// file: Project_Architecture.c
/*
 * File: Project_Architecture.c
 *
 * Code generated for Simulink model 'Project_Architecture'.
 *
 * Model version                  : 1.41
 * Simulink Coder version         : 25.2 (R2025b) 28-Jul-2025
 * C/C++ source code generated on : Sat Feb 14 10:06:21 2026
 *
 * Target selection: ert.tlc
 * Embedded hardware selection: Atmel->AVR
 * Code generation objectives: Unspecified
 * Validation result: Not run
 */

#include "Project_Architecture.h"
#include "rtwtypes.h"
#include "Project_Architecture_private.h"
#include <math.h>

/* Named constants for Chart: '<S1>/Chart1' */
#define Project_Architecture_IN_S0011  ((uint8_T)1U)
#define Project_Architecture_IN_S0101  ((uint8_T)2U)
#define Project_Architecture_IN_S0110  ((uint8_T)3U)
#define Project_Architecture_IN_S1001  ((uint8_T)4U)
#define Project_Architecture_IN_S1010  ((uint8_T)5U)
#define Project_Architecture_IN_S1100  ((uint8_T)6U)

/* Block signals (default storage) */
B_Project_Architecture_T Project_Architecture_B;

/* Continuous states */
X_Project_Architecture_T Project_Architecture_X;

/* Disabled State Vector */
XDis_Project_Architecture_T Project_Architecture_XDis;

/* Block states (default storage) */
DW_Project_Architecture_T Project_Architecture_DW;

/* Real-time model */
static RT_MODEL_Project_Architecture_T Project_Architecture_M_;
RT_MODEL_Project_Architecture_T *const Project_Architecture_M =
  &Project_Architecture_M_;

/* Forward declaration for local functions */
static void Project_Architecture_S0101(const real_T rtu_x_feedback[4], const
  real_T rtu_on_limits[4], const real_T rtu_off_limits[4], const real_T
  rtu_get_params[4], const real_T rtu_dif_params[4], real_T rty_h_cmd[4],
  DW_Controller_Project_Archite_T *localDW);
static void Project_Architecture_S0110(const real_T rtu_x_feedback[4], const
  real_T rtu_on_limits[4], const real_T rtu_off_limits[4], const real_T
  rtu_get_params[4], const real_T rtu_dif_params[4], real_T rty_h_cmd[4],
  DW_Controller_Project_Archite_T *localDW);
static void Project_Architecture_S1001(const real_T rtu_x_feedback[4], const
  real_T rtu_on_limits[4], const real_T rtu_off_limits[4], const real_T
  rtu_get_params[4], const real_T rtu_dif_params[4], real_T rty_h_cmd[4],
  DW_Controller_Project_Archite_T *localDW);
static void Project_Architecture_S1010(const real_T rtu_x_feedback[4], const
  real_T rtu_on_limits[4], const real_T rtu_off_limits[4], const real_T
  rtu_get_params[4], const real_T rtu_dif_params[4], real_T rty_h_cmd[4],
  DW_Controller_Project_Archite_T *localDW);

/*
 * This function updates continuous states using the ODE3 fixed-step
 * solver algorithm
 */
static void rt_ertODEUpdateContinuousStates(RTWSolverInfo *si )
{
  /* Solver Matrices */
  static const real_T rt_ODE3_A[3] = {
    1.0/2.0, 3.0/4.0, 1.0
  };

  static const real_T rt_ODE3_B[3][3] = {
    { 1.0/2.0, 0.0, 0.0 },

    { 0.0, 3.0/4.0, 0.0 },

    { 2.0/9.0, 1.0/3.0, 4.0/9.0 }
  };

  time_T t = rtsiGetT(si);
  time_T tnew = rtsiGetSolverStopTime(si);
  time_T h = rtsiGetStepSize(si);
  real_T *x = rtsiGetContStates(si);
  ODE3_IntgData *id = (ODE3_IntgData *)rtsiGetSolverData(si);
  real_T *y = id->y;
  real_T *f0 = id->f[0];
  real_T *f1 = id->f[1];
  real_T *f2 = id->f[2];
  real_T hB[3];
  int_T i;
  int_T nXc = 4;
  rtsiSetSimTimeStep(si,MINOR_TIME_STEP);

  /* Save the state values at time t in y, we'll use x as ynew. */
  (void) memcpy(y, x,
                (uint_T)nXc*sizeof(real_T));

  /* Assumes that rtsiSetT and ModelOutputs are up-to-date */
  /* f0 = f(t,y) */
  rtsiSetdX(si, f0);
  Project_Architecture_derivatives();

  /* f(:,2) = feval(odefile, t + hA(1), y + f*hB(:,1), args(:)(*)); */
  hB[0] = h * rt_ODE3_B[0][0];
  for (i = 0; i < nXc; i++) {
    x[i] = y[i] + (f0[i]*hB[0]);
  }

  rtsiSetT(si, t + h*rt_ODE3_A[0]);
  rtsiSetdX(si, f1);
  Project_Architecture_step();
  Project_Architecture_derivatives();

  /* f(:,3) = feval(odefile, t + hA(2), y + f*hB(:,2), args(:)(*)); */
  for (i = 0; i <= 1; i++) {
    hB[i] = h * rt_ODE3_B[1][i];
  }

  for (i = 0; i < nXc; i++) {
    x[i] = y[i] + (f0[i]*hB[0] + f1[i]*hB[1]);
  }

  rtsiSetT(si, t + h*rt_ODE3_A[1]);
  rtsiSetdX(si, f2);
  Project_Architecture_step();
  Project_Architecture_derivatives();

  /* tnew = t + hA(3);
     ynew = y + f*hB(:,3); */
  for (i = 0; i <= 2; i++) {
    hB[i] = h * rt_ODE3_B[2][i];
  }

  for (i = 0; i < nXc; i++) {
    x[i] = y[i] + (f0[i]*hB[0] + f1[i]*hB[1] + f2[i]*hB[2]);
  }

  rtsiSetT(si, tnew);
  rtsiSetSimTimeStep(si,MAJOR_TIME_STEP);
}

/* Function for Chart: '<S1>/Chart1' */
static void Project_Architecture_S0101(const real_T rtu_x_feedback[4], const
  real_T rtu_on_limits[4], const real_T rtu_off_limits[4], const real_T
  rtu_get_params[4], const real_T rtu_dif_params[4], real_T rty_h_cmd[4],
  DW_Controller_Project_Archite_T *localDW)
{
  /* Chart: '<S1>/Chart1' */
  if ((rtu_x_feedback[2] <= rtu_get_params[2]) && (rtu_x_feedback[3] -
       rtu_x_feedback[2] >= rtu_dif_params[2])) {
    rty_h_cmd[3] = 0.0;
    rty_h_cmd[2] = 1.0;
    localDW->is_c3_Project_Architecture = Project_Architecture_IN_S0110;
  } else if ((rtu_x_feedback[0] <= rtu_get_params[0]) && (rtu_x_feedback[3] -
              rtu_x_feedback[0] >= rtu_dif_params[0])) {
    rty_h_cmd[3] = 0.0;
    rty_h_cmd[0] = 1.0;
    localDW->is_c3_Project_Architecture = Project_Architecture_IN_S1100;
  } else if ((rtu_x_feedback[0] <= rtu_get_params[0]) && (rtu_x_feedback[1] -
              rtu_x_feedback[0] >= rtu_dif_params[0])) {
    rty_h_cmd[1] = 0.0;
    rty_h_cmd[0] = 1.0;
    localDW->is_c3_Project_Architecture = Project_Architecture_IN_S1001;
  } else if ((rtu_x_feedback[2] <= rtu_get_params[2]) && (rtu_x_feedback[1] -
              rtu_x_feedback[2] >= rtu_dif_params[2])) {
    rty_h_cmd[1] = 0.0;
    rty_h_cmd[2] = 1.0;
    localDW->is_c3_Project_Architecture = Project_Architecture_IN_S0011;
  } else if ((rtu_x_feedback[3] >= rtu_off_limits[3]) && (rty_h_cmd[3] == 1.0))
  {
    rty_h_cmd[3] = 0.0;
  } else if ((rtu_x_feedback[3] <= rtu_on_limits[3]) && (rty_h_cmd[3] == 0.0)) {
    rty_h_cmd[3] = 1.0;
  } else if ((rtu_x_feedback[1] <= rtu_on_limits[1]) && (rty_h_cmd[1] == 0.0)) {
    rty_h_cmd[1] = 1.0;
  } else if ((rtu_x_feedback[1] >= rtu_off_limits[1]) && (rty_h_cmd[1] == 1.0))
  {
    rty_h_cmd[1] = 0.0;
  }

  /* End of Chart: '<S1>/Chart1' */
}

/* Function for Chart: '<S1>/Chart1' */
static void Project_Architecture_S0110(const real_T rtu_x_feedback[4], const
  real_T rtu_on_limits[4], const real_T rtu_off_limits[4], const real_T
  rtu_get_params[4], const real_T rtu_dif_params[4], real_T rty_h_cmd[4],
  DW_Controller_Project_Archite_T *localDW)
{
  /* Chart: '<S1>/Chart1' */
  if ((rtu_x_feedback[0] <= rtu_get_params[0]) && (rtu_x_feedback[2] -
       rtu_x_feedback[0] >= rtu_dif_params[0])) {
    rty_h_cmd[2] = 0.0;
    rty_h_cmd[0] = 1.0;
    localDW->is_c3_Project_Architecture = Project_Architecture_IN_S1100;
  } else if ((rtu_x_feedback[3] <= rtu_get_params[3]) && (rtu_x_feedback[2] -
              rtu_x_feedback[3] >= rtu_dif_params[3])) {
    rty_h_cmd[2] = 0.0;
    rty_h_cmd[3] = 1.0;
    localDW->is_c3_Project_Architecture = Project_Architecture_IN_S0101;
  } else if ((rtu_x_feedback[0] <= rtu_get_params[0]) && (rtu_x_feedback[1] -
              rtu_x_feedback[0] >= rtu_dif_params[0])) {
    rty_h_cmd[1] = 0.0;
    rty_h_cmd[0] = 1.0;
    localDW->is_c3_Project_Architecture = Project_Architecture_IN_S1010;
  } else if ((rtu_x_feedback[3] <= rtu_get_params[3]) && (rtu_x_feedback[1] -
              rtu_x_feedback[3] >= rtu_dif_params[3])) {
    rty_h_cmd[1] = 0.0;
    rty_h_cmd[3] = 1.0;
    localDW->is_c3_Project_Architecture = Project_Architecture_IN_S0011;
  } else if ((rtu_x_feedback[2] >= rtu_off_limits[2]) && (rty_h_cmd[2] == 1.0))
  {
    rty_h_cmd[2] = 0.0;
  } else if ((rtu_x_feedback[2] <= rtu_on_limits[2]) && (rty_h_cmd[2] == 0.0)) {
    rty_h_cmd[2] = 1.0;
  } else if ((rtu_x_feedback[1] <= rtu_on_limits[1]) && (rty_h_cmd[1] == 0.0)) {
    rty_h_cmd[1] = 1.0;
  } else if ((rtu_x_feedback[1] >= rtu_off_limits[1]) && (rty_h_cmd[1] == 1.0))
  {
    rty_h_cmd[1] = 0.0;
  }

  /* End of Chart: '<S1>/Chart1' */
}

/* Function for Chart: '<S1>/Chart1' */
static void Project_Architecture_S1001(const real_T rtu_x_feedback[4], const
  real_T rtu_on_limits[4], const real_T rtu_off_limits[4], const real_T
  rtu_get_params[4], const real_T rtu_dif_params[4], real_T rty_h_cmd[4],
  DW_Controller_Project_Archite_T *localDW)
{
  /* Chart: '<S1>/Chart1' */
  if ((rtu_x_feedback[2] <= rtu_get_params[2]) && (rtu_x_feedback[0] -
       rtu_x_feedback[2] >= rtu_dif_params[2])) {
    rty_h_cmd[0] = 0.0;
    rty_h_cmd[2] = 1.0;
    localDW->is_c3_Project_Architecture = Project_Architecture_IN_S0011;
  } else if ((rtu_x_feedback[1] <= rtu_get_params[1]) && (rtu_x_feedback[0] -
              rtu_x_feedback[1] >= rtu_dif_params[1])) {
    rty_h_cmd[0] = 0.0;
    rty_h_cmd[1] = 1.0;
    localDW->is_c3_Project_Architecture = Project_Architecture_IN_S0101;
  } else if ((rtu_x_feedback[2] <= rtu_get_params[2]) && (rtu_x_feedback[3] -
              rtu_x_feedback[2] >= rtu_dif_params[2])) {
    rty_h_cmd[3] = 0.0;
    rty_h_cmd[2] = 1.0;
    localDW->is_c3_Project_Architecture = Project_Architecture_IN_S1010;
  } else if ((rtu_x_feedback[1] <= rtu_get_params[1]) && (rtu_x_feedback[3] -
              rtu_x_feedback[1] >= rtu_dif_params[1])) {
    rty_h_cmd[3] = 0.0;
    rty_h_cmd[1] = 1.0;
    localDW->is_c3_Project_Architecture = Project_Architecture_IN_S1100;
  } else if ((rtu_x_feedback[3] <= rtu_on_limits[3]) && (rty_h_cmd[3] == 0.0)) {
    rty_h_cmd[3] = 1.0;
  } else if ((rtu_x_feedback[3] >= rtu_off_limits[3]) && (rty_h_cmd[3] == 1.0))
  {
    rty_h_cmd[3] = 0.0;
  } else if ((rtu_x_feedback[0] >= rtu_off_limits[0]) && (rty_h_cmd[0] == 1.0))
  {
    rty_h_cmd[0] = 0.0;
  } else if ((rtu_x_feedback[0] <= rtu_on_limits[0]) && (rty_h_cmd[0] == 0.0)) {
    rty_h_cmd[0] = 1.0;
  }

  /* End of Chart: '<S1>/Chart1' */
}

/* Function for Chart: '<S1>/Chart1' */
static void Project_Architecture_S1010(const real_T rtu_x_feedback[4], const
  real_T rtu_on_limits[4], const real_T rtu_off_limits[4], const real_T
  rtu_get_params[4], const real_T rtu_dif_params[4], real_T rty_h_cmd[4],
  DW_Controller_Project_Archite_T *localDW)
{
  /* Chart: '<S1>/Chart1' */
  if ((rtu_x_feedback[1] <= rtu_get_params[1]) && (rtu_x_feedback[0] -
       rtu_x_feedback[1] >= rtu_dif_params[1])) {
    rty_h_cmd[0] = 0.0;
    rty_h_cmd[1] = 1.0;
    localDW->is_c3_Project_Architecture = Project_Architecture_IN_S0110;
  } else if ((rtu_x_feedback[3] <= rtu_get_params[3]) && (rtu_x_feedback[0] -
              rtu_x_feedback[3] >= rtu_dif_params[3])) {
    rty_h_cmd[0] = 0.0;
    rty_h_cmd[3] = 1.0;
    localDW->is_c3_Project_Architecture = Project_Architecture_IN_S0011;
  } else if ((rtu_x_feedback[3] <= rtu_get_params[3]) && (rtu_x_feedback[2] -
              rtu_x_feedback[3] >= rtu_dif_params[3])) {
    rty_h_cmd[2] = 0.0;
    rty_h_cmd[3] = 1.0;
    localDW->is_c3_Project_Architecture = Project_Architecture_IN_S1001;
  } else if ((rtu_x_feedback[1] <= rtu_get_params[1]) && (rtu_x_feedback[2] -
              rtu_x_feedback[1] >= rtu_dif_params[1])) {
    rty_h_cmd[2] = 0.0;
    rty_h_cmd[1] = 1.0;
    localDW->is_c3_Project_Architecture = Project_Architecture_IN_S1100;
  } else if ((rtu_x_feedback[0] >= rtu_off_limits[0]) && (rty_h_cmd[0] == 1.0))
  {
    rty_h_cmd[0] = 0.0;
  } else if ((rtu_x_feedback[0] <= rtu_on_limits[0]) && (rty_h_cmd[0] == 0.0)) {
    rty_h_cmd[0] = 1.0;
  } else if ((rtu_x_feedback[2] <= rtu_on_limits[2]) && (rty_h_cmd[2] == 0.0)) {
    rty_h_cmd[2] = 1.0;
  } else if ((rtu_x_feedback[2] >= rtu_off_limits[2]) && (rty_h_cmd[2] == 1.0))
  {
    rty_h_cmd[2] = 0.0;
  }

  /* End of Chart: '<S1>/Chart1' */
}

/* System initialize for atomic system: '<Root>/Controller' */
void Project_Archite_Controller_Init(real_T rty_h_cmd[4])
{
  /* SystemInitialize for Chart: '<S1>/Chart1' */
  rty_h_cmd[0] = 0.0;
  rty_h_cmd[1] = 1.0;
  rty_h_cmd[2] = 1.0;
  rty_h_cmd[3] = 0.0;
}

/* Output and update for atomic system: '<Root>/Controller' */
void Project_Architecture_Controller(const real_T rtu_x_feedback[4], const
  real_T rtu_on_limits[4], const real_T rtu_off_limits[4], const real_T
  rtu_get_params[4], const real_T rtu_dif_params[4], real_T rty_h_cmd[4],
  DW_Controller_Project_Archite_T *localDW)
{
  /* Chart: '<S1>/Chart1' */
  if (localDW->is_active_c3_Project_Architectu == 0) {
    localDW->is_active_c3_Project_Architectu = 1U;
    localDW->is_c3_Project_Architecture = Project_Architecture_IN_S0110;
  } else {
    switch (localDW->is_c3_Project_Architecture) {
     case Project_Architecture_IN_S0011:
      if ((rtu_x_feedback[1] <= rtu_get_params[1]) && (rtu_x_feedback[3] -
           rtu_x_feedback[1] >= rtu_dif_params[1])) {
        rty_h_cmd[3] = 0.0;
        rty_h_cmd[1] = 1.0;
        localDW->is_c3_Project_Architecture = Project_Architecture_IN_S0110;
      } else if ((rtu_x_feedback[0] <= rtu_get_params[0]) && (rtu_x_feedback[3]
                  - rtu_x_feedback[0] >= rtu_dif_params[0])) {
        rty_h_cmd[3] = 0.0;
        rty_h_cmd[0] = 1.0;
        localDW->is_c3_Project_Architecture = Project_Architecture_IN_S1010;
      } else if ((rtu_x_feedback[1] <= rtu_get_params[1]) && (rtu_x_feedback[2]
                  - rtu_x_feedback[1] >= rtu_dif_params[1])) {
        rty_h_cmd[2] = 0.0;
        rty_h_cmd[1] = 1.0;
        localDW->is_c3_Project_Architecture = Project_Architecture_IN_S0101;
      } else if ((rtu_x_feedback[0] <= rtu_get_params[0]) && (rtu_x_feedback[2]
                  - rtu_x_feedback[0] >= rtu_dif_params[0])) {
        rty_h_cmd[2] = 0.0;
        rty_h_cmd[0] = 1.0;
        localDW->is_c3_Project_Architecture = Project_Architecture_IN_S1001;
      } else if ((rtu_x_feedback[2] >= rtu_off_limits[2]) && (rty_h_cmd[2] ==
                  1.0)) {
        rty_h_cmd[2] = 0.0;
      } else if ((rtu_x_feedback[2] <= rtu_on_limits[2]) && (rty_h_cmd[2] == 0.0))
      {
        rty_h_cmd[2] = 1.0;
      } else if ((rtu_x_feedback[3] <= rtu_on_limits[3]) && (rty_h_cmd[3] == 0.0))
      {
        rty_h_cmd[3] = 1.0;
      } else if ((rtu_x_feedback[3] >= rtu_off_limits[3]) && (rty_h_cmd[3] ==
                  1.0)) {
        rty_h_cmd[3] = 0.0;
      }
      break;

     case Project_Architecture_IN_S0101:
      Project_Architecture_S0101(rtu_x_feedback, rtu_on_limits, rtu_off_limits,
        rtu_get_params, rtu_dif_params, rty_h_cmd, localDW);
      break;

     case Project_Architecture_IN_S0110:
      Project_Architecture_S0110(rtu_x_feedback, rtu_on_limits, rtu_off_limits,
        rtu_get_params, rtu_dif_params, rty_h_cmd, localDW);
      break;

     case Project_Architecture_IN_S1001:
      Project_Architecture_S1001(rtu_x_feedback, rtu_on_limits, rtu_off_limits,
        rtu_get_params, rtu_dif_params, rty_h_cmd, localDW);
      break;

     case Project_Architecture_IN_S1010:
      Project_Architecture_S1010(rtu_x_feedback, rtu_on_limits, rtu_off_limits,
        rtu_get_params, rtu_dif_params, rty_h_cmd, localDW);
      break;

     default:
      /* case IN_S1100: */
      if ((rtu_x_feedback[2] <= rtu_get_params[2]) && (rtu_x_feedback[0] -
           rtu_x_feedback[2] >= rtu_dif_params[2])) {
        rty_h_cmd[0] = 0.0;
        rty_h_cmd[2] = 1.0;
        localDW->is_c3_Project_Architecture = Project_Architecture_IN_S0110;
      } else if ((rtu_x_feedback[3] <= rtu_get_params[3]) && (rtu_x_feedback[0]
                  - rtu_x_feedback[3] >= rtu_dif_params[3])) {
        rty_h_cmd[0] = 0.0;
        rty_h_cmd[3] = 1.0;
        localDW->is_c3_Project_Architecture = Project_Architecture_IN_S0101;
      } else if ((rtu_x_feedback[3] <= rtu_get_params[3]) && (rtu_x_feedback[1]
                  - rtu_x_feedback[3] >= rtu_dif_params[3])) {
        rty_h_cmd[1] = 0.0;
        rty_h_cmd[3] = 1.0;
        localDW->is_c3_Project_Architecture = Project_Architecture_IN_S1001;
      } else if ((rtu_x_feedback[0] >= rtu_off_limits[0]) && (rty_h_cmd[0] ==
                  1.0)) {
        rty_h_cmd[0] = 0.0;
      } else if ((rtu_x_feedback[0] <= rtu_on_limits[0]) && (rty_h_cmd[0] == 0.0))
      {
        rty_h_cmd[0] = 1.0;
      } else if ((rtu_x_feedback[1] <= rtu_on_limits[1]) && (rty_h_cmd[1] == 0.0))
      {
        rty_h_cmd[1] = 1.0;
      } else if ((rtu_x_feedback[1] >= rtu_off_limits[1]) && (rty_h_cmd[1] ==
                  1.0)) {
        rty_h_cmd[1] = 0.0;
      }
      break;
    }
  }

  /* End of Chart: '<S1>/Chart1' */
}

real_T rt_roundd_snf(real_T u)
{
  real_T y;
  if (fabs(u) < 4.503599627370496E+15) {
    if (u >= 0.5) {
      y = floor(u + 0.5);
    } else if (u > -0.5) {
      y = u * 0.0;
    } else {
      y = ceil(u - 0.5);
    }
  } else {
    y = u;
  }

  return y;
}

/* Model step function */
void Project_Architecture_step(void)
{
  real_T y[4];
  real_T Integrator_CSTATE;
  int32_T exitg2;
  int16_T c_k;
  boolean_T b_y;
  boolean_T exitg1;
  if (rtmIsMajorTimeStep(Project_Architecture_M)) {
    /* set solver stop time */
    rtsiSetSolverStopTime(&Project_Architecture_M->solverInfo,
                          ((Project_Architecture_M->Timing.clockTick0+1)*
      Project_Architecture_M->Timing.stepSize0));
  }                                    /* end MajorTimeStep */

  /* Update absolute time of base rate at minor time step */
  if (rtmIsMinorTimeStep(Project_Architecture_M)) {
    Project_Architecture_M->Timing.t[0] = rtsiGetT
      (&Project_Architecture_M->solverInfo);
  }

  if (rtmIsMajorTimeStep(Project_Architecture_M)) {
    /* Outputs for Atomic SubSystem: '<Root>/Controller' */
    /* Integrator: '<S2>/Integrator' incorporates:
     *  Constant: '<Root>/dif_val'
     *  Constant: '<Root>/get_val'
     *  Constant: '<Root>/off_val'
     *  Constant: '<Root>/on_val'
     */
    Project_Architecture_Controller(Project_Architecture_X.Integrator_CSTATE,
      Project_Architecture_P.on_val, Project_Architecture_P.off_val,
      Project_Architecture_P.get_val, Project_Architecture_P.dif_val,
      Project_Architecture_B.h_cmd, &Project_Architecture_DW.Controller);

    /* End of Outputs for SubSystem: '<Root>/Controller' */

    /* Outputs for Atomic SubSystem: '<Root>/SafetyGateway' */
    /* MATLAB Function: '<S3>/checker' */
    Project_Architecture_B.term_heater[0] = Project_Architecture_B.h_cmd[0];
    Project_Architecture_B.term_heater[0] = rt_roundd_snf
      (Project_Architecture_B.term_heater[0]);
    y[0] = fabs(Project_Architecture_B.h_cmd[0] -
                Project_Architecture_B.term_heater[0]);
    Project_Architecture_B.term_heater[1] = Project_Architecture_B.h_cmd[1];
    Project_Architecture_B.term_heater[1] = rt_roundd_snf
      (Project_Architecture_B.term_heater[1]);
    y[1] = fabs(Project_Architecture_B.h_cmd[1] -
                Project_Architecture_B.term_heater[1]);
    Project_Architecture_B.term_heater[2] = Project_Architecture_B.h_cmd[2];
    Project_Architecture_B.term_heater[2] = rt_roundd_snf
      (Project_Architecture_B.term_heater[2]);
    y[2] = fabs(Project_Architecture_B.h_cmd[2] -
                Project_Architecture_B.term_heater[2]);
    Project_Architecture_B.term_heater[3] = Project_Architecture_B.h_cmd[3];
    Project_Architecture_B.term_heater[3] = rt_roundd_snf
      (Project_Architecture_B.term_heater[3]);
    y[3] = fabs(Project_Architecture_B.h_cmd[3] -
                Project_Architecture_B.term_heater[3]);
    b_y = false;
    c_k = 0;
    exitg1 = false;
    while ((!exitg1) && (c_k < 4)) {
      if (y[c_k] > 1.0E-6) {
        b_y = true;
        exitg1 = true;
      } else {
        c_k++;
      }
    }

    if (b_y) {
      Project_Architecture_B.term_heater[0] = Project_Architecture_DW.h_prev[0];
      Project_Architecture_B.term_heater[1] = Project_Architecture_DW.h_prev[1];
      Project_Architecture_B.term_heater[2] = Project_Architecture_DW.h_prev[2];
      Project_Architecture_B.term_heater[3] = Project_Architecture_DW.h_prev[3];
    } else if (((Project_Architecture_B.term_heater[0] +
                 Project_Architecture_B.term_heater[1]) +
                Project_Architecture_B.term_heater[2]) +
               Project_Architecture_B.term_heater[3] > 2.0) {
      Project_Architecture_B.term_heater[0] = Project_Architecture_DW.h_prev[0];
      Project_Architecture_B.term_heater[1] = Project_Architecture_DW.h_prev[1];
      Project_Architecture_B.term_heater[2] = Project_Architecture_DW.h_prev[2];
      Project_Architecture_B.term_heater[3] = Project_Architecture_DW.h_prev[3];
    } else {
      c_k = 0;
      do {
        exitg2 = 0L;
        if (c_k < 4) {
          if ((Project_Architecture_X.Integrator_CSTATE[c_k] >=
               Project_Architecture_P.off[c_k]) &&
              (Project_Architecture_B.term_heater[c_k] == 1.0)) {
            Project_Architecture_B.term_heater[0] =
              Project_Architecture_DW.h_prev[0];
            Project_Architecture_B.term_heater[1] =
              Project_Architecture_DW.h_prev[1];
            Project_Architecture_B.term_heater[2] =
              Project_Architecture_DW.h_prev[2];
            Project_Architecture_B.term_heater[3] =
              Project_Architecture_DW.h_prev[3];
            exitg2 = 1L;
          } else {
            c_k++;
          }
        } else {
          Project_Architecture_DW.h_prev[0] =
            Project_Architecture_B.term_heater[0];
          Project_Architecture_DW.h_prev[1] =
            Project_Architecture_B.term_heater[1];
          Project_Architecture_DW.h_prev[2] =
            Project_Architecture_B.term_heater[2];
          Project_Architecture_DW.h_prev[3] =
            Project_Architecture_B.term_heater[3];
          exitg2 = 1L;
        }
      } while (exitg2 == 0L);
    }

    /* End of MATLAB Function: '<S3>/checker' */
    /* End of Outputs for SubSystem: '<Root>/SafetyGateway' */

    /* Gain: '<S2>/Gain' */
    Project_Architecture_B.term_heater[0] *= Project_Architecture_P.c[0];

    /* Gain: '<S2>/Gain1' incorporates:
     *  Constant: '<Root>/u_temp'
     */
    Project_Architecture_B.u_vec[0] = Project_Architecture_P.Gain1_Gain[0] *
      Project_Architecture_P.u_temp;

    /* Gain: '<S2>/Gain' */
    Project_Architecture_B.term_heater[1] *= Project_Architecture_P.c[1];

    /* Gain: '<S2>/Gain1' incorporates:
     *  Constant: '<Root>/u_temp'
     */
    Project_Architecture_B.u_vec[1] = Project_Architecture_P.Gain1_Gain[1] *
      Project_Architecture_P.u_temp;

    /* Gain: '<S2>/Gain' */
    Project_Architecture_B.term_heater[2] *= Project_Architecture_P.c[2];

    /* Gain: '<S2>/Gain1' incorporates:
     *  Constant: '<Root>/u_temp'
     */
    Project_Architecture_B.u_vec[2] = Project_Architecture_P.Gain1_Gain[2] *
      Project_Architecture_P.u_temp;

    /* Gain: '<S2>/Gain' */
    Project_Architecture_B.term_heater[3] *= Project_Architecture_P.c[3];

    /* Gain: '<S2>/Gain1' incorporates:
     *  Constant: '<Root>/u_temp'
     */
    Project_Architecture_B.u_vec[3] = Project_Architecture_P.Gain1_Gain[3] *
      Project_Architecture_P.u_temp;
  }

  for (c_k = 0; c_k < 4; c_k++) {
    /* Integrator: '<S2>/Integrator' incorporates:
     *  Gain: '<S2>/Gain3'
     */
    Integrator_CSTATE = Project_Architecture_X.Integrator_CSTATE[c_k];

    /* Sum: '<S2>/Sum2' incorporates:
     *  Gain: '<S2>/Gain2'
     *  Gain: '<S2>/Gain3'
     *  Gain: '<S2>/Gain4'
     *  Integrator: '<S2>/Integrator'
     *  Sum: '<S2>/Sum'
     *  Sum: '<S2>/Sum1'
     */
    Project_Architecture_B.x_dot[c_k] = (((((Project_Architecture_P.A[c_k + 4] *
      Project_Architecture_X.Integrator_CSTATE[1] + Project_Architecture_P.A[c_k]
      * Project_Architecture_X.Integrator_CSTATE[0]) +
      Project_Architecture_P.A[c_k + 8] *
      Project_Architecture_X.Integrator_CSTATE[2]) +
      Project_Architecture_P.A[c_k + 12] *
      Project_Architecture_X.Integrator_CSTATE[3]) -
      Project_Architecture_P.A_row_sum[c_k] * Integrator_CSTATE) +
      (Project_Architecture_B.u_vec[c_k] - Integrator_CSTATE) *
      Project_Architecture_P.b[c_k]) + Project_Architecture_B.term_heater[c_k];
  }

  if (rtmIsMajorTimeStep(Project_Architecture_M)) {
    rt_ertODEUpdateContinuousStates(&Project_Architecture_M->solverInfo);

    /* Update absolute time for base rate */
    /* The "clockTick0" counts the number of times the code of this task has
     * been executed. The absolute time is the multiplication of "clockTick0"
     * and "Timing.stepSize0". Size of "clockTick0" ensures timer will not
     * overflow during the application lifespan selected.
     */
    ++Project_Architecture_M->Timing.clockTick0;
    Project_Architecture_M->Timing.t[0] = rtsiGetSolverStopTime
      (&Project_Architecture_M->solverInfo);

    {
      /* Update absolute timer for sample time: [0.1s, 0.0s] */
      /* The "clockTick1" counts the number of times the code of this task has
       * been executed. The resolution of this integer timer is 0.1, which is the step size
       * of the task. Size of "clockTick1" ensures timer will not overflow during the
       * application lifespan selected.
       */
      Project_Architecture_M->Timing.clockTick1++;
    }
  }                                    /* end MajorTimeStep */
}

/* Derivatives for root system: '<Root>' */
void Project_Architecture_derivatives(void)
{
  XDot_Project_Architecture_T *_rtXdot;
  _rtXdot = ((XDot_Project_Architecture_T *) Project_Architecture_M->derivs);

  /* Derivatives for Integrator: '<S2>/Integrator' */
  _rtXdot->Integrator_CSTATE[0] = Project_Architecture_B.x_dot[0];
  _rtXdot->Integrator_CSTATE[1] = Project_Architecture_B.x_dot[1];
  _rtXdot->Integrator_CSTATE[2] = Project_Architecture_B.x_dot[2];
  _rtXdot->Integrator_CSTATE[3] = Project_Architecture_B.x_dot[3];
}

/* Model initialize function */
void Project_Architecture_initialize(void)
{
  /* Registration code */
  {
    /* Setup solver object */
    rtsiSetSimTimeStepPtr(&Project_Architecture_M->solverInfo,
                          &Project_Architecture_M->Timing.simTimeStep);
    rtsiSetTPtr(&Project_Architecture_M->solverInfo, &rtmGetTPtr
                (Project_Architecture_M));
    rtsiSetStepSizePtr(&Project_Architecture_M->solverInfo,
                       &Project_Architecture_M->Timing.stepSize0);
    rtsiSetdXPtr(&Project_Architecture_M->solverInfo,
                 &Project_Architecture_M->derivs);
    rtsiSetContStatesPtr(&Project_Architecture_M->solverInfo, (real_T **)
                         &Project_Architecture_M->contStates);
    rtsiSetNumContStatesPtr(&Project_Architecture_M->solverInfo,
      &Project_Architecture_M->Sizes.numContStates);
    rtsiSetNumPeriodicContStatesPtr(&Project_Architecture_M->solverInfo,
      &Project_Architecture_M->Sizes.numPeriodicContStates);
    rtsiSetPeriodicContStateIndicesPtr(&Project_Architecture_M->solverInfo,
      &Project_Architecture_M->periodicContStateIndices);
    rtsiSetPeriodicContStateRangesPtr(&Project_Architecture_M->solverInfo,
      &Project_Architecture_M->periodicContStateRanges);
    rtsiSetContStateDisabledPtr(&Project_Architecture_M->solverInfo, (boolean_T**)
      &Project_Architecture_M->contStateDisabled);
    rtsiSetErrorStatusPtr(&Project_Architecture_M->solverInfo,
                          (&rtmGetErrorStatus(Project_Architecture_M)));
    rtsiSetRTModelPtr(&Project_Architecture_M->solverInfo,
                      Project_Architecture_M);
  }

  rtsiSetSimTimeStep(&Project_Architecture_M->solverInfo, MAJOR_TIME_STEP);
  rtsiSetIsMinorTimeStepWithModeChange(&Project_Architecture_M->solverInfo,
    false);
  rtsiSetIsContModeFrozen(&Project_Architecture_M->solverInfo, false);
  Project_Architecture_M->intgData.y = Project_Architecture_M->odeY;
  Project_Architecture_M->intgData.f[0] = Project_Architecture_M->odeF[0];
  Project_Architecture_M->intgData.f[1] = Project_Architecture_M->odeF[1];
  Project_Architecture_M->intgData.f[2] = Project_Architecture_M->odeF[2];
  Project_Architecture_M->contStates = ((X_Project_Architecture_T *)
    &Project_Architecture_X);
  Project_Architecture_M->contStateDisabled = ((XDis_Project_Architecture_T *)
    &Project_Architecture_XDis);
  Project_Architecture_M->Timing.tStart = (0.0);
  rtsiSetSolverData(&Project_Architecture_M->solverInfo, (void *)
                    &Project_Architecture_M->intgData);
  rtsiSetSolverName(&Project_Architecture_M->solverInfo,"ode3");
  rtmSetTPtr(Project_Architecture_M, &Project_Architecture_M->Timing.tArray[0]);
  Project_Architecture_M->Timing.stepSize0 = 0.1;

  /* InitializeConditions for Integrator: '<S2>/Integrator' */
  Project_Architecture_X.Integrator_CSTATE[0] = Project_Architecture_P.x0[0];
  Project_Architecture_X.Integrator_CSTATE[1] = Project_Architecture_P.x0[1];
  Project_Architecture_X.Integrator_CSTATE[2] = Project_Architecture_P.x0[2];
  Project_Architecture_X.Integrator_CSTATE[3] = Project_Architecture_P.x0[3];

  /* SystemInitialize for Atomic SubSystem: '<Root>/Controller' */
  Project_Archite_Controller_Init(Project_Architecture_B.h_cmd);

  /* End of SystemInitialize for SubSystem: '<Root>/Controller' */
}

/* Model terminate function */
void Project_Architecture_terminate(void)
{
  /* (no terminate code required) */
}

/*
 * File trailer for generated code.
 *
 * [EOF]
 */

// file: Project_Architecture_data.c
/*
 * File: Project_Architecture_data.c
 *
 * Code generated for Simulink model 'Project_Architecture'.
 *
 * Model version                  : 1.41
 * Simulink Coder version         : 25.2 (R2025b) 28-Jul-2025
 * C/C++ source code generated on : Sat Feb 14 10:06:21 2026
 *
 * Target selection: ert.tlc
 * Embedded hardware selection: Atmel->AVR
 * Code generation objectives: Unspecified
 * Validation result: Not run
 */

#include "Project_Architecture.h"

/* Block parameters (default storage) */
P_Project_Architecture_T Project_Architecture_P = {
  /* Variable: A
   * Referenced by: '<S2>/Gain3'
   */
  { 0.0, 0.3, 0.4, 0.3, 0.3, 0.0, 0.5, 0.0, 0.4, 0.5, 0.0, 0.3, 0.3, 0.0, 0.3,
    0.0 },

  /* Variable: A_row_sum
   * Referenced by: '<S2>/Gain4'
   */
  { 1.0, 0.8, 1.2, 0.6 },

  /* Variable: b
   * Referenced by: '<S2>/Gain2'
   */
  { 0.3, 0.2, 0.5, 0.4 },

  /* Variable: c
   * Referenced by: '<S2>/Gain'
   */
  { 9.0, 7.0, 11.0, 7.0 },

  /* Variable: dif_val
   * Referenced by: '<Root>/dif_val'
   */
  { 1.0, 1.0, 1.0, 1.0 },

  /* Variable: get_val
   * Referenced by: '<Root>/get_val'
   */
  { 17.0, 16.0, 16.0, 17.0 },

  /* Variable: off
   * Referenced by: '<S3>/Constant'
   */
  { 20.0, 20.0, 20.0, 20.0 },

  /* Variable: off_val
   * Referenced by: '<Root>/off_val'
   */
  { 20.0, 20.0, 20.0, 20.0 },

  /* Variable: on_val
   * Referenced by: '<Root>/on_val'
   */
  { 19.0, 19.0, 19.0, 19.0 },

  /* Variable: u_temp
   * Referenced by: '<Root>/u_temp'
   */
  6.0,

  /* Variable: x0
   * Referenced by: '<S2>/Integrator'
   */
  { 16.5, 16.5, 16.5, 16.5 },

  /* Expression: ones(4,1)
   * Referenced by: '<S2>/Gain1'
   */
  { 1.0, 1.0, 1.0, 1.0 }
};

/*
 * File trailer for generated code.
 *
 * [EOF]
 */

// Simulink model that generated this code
simulink model "Project_Architecture"  (R2025b)
settings: Solver=FixedStepAuto  StartTime=0.0  StopTime=200  FixedStep=0.1  RelTol=1e-3
values from neighbouring files (symbols this model uses):
  A = [0.00, 0.30, 0.40, 0.30 ... (first row only)    [init_params.m]
  A_row_sum = sum(A, 2)    [init_params.m]
  b = [0.30; 0.20; 0.50; 0.40]    [init_params.m]
  c = [9.00; 7.00; 11.00; 7.00]    [init_params.m]
  dif_val = dif    [init_params.m]
  get_val = get    [init_params.m]
  off_val = off    [init_params.m]
  on_val = on    [init_params.m]
  u_temp = 6    [init_params.m]
  x0 = [16.5; 16.5; 16.5; 16.5]    [init_params.m]

== system Project_Architecture ==
  Controller : Subsystem  TreatAsAtomicUnit=on  SystemSampleTime=0.1
  RoomModel : Subsystem
  SafetyGateway : Subsystem  TreatAsAtomicUnit=on  SystemSampleTime=0.1
  Scope : Scope  NumInputPorts=4
  dif_val : Constant  Value=dif_val
  get_val : Constant  Value=get_val
  off_val : Constant  Value=off_val
  on_val : Constant  Value=on_val
  u_temp : Constant  Value=u_temp
  wires:
  u_temp/1 -> RoomModel/1(u_temp)
  SafetyGateway/1(h_act) -> RoomModel/2(h_act), Scope/3  "Heaters <4>"
  RoomModel/1(x_temp) -> Scope/1, SafetyGateway/1(x_temp), Controller/1(x_feedback)  "Temperature <4>"
  Controller/1(h_cmd) -> SafetyGateway/2(h_cmd), Scope/2
  SafetyGateway/2(unsafe_flag) -> Scope/4
  on_val/1 -> Controller/2(on_limits)
  off_val/1 -> Controller/3(off_limits)
  get_val/1 -> Controller/4(get_params)
  dif_val/1 -> Controller/5(dif_params)

== system Project_Architecture/Controller ==
  x_feedback : Inport
  on_limits : Inport  Port=2
  off_limits : Inport  Port=3
  get_params : Inport  Port=4
  dif_params : Inport  Port=5
  Chart1 : Stateflow chart  TreatAsAtomicUnit=on
  h_cmd : Outport
  h : Outport  Port=2
  wires:
  x_feedback/1 -> Chart1/1(x_feedback)
  Chart1/1(h_cmd) -> h_cmd/1
  off_limits/1 -> Chart1/3(off_limits)
  get_params/1 -> Chart1/4(get_params)
  dif_params/1 -> Chart1/5(dif_params)
  on_limits/1 -> Chart1/2(on_limits)

== system Project_Architecture/RoomModel ==
  u_temp : Inport  PortDimensions=1
  h_act : Inport  Port=2  PortDimensions=4
  Gain : Gain  Gain=c
  Gain1 : Gain  Gain=ones(4,1)
  Gain2 : Gain  Gain=b
  Gain3 : Gain  Gain=A  Multiplication=Matrix(K*u)
  Gain4 : Gain  Gain=A_row_sum
  Integrator : Integrator  InitialCondition=x0
  Sum : Sum  Inputs=|+-
  Sum1 : Sum  Inputs=|+-
  Sum2 : Sum  Inputs=|+++
  x_temp : Outport  PortDimensions=4
  wires:
  u_temp/1 -> Gain1/1
  h_act/1 -> Gain/1
  Gain/1 -> Sum2/3  "term_heater"
  Gain1/1 -> Sum/1  "u_vec"
  Sum/1 -> Gain2/1
  Gain4/1 -> Sum1/2  "Axi"
  Gain3/1 -> Sum1/1  "Ax"
  Sum1/1 -> Sum2/1  "term_neighbors"
  Gain2/1 -> Sum2/2  "term_outside"
  Sum2/1 -> Integrator/1  "x_dot"
  Integrator/1 -> x_temp/1, [A1]
  [A1] -> Gain3/1
  [A1] -> Sum/2
  [A1] -> Gain4/1

== system Project_Architecture/SafetyGateway ==
  x_temp : Inport  PortDimensions=4
  h_cmd : Inport  Port=2  PortDimensions=4
  Constant : Constant  Value=off
  checker : MATLAB Function  TreatAsAtomicUnit=on
  h_act : Outport  PortDimensions=4
  unsafe_flag : Outport  Port=2  PortDimensions=1
  wires:
  x_temp/1 -> checker/1(x_temp)
  h_cmd/1 -> checker/2(h_cmd)
  checker/1(h_act) -> h_act/1
  checker/2(unsafe_flag) -> unsafe_flag/1
  Constant/1 -> checker/3(off)

== matlab function Project_Architecture/SafetyGateway/checker ==
function [h_act, unsafe_flag] = checker(x_temp, h_cmd, off)

persistent h_prev
if isempty(h_prev)
    h_prev = zeros(4,1);
end

unsafe_flag = 0;

% Force column vectors
x = x_temp(:);
h = h_cmd(:);

h_rounded = round(h);

if any(abs(h - h_rounded) > 1e-6)
    unsafe_flag = 1;
    h_act = h_prev;
    return;
end

h = h_rounded;

if sum(h) > 2
    unsafe_flag = 1;
    h_act = h_prev;
    return;
end

for i = 1:4
    if x(i) >= off(i) && h(i) == 1
        unsafe_flag = 1;
        h_act = h_prev;
        return;
    end
end

h_act = h;
h_prev = h_act;

== stateflow chart Project_Architecture/Controller/Chart1 ==
  settings: sampleTime=0.01
  state S1100
    state S3
    (default) -> S1100.S3
    S1100.S3 -> S1100.S3 [order 4] : [x_feedback(2)>=off_limits(2) && h_cmd(2) == 1]{h_cmd(2) = 0;}
    S1100.S3 -> S1100.S3 [order 3] : [x_feedback(2) <=on_limits(2) && h_cmd(2) == 0]{h_cmd(2) = 1;}
    S1100.S3 -> S1100.S3 [order 2] : [x_feedback(1) <=on_limits(1) && h_cmd(1) == 0]{h_cmd(1) = 1;}
    S1100.S3 -> S1100.S3 [order 1] : [x_feedback(1)>=off_limits(1) && h_cmd(1) == 1]{h_cmd(1) = 0;}
  state S0110
    state S3
    (default) -> S0110.S3
    S0110.S3 -> S0110.S3 [order 4] : [x_feedback(2)>=off_limits(2) && h_cmd(2) == 1]{h_cmd(2) = 0;}
    S0110.S3 -> S0110.S3 [order 3] : [x_feedback(2) <=on_limits(2) && h_cmd(2) == 0]{h_cmd(2) = 1;}
    S0110.S3 -> S0110.S3 [order 2] : [x_feedback(3) <=on_limits(3) && h_cmd(3) == 0]{h_cmd(3) = 1;}
    S0110.S3 -> S0110.S3 [order 1] : [x_feedback(3)>=off_limits(3) && h_cmd(3) == 1]{h_cmd(3) = 0;}
  state S0101
    state S3
    (default) -> S0101.S3
    S0101.S3 -> S0101.S3 [order 4] : [x_feedback(2)>=off_limits(2) && h_cmd(2) == 1]{h_cmd(2) = 0;}
    S0101.S3 -> S0101.S3 [order 3] : [x_feedback(2) <=on_limits(2) && h_cmd(2) == 0]{h_cmd(2) = 1;}
    S0101.S3 -> S0101.S3 [order 2] : [x_feedback(4) <=on_limits(4) && h_cmd(4) == 0]{h_cmd(4) = 1;}
    S0101.S3 -> S0101.S3 [order 1] : [x_feedback(4)>=off_limits(4) && h_cmd(4) == 1]{h_cmd(4) = 0;}
  state S0011
    state S3
    S0011.S3 -> S0011.S3 [order 4] : [x_feedback(4)>=off_limits(4) && h_cmd(4) == 1]{h_cmd(4) = 0;}
    S0011.S3 -> S0011.S3 [order 3] : [x_feedback(4) <=on_limits(4) && h_cmd(4) == 0]{h_cmd(4) = 1;}
    S0011.S3 -> S0011.S3 [order 2] : [x_feedback(3) <=on_limits(3) && h_cmd(3) == 0]{h_cmd(3) = 1;}
    S0011.S3 -> S0011.S3 [order 1] : [x_feedback(3)>=off_limits(3) && h_cmd(3) == 1]{h_cmd(3) = 0;}
  state S1001
    state S3
    (default) -> S1001.S3
    S1001.S3 -> S1001.S3 [order 2] : [x_feedback(4)>=off_limits(4) && h_cmd(4) == 1]{h_cmd(4) = 0;}
    S1001.S3 -> S1001.S3 [order 1] : [x_feedback(4) <=on_limits(4) && h_cmd(4) == 0]{h_cmd(4) = 1;}
    S1001.S3 -> S1001.S3 [order 4] : [x_feedback(1) <=on_limits(1) && h_cmd(1) == 0]{h_cmd(1) = 1;}
    S1001.S3 -> S1001.S3 [order 3] : [x_feedback(1)>=off_limits(1) && h_cmd(1) == 1]{h_cmd(1) = 0;}
  state S1010
    state S3
    (default) -> S1010.S3
    S1010.S3 -> S1010.S3 [order 4] : [x_feedback(3)>=off_limits(3) && h_cmd(3) == 1]{h_cmd(3) = 0;}
    S1010.S3 -> S1010.S3 [order 3] : [x_feedback(3) <=on_limits(3) && h_cmd(3) == 0]{h_cmd(3) = 1;}
    S1010.S3 -> S1010.S3 [order 2] : [x_feedback(1) <=on_limits(1) && h_cmd(1) == 0]{h_cmd(1) = 1;}
    S1010.S3 -> S1010.S3 [order 1] : [x_feedback(1)>=off_limits(1) && h_cmd(1) == 1]{h_cmd(1) = 0;}
  (default) -> S0110 [order 1]
  S0110 -> S1100 [order 1] : [x_feedback(1) <=get_params(1) && x_feedback(3) - x_feedback(1) >= dif_params(1)]{h_cmd(3) = 0; h_cmd(1) = 1;}
  S1100 -> S0110 [order 1] : [x_feedback(3) <=get_params(3) && x_feedback(1) - x_feedback(3) >= dif_params(3)]{h_cmd(1) = 0; h_cmd(3) = 1;}
  S1001 -> S1100 [order 4] : [x_feedback(2) <=get_params(2) && x_feedback(4) - x_feedback(2) >= dif_params(2)]{h_cmd(4) = 0; h_cmd(2) = 1;}
  S0110 -> S1010 [order 3] : [x_feedback(1) <=get_params(1) && x_feedback(2) - x_feedback(1) >= dif_params(1)]{h_cmd(2) = 0; h_cmd(1) = 1;}
  S1100 -> S1001 [order 3] : [x_feedback(4) <=get_params(4) && x_feedback(2) - x_feedback(4) >= dif_params(4)]{h_cmd(2) = 0; h_cmd(4) = 1;}
  S0101 -> S0110 [order 1] : [x_feedback(3) <=get_params(3) && x_feedback(4) - x_feedback(3) >= dif_params(3)]{h_cmd(4) = 0; h_cmd(3) = 1;}
  S1010 -> S0110 [order 1] : [x_feedback(2) <=get_params(2) && x_feedback(1) - x_feedback(2) >= dif_params(2)]{h_cmd(1) = 0; h_cmd(2) = 1;}
  S1010 -> S1100 [order 4] : [x_feedback(2) <=get_params(2) && x_feedback(3) - x_feedback(2) >= dif_params(2)]{h_cmd(3) = 0; h_cmd(2) = 1;}
  S1100 -> S0101 [order 2] : [x_feedback(4) <=get_params(4) && x_feedback(1) - x_feedback(4) >= dif_params(4)]{h_cmd(1) = 0; h_cmd(4) = 1;}
  S0101 -> S1100 [order 2] : [x_feedback(1) <=get_params(1) && x_feedback(4) - x_feedback(1) >= dif_params(1)]{h_cmd(4) = 0; h_cmd(1) = 1;}
  S0110 -> S0101 [order 2] : [x_feedback(4) <=get_params(4) && x_feedback(3) - x_feedback(4) >= dif_params(4)]{h_cmd(3) = 0; h_cmd(4) = 1;}
  (default) -> S1010 [order 3] : [x_feedback(3) <=get_params(3) && x_feedback(2) - x_feedback(3) >= dif_params(3)]{h_cmd(2) = 0; h_cmd(3) = 1;}
  S0011 -> S0110 [order 1] : [x_feedback(2) <=get_params(2) && x_feedback(4) - x_feedback(2) >= dif_params(2)]{h_cmd(4) = 0; h_cmd(2) = 1;}
  S0110 -> S0011 [order 4] : [x_feedback(4) <=get_params(4) && x_feedback(2) - x_feedback(4) >= dif_params(4)]{h_cmd(2) = 0; h_cmd(4) = 1;}
  (default) -> S0011.S3 [order 2]
  S0011 -> S0101 [order 3] : [x_feedback(2) <=get_params(2) && x_feedback(3) - x_feedback(2) >= dif_params(2)]{h_cmd(3) = 0; h_cmd(2) = 1;}
  S0101 -> S0011 [order 4] : [x_feedback(3) <=get_params(3) && x_feedback(2) - x_feedback(3) >= dif_params(3)]{h_cmd(2) = 0; h_cmd(3) = 1;}
  S1001 -> S0011 [order 1] : [x_feedback(3) <=get_params(3) && x_feedback(1) - x_feedback(3) >= dif_params(3)]{h_cmd(1) = 0; h_cmd(3) = 1;}
  S0011 -> S1001 [order 4] : [x_feedback(1) <=get_params(1) && x_feedback(3) - x_feedback(1) >= dif_params(1)]{h_cmd(3) = 0; h_cmd(1) = 1;}
  S0101 -> S1001 [order 3] : [x_feedback(1) <=get_params(1) && x_feedback(2) - x_feedback(1) >= dif_params(1)]{h_cmd(2) = 0; h_cmd(1) = 1;}
  S1001 -> S0101 [order 2] : [x_feedback(2) <=get_params(2) && x_feedback(1) - x_feedback(2) >= dif_params(2)]{h_cmd(1) = 0; h_cmd(2) = 1;}
  S1010 -> S0011 [order 2] : [x_feedback(4) <=get_params(4) && x_feedback(1) - x_feedback(4) >= dif_params(4)]{h_cmd(1) = 0; h_cmd(4) = 1;}
  S0011 -> S1010 [order 2] : [x_feedback(1) <=get_params(1) && x_feedback(4) - x_feedback(1) >= dif_params(1)]{h_cmd(4) = 0; h_cmd(1) = 1;}
  S1001 -> S1010 [order 3] : [x_feedback(3) <=get_params(3) && x_feedback(4) - x_feedback(3) >= dif_params(3)]{h_cmd(4) = 0; h_cmd(3) = 1;}
  S1010 -> S1001 [order 3] : [x_feedback(4) <=get_params(4) && x_feedback(3) - x_feedback(4) >= dif_params(4)]{h_cmd(3) = 0; h_cmd(4) = 1;}
  data: x_feedback input size=[1 4]; h_cmd output size=[1 4] =[0 1 1 0]; on_limits input size=[1 4]; off_limits input size=[1 4]; get_params input size=[1 4]; dif_params input size=[1 4]
